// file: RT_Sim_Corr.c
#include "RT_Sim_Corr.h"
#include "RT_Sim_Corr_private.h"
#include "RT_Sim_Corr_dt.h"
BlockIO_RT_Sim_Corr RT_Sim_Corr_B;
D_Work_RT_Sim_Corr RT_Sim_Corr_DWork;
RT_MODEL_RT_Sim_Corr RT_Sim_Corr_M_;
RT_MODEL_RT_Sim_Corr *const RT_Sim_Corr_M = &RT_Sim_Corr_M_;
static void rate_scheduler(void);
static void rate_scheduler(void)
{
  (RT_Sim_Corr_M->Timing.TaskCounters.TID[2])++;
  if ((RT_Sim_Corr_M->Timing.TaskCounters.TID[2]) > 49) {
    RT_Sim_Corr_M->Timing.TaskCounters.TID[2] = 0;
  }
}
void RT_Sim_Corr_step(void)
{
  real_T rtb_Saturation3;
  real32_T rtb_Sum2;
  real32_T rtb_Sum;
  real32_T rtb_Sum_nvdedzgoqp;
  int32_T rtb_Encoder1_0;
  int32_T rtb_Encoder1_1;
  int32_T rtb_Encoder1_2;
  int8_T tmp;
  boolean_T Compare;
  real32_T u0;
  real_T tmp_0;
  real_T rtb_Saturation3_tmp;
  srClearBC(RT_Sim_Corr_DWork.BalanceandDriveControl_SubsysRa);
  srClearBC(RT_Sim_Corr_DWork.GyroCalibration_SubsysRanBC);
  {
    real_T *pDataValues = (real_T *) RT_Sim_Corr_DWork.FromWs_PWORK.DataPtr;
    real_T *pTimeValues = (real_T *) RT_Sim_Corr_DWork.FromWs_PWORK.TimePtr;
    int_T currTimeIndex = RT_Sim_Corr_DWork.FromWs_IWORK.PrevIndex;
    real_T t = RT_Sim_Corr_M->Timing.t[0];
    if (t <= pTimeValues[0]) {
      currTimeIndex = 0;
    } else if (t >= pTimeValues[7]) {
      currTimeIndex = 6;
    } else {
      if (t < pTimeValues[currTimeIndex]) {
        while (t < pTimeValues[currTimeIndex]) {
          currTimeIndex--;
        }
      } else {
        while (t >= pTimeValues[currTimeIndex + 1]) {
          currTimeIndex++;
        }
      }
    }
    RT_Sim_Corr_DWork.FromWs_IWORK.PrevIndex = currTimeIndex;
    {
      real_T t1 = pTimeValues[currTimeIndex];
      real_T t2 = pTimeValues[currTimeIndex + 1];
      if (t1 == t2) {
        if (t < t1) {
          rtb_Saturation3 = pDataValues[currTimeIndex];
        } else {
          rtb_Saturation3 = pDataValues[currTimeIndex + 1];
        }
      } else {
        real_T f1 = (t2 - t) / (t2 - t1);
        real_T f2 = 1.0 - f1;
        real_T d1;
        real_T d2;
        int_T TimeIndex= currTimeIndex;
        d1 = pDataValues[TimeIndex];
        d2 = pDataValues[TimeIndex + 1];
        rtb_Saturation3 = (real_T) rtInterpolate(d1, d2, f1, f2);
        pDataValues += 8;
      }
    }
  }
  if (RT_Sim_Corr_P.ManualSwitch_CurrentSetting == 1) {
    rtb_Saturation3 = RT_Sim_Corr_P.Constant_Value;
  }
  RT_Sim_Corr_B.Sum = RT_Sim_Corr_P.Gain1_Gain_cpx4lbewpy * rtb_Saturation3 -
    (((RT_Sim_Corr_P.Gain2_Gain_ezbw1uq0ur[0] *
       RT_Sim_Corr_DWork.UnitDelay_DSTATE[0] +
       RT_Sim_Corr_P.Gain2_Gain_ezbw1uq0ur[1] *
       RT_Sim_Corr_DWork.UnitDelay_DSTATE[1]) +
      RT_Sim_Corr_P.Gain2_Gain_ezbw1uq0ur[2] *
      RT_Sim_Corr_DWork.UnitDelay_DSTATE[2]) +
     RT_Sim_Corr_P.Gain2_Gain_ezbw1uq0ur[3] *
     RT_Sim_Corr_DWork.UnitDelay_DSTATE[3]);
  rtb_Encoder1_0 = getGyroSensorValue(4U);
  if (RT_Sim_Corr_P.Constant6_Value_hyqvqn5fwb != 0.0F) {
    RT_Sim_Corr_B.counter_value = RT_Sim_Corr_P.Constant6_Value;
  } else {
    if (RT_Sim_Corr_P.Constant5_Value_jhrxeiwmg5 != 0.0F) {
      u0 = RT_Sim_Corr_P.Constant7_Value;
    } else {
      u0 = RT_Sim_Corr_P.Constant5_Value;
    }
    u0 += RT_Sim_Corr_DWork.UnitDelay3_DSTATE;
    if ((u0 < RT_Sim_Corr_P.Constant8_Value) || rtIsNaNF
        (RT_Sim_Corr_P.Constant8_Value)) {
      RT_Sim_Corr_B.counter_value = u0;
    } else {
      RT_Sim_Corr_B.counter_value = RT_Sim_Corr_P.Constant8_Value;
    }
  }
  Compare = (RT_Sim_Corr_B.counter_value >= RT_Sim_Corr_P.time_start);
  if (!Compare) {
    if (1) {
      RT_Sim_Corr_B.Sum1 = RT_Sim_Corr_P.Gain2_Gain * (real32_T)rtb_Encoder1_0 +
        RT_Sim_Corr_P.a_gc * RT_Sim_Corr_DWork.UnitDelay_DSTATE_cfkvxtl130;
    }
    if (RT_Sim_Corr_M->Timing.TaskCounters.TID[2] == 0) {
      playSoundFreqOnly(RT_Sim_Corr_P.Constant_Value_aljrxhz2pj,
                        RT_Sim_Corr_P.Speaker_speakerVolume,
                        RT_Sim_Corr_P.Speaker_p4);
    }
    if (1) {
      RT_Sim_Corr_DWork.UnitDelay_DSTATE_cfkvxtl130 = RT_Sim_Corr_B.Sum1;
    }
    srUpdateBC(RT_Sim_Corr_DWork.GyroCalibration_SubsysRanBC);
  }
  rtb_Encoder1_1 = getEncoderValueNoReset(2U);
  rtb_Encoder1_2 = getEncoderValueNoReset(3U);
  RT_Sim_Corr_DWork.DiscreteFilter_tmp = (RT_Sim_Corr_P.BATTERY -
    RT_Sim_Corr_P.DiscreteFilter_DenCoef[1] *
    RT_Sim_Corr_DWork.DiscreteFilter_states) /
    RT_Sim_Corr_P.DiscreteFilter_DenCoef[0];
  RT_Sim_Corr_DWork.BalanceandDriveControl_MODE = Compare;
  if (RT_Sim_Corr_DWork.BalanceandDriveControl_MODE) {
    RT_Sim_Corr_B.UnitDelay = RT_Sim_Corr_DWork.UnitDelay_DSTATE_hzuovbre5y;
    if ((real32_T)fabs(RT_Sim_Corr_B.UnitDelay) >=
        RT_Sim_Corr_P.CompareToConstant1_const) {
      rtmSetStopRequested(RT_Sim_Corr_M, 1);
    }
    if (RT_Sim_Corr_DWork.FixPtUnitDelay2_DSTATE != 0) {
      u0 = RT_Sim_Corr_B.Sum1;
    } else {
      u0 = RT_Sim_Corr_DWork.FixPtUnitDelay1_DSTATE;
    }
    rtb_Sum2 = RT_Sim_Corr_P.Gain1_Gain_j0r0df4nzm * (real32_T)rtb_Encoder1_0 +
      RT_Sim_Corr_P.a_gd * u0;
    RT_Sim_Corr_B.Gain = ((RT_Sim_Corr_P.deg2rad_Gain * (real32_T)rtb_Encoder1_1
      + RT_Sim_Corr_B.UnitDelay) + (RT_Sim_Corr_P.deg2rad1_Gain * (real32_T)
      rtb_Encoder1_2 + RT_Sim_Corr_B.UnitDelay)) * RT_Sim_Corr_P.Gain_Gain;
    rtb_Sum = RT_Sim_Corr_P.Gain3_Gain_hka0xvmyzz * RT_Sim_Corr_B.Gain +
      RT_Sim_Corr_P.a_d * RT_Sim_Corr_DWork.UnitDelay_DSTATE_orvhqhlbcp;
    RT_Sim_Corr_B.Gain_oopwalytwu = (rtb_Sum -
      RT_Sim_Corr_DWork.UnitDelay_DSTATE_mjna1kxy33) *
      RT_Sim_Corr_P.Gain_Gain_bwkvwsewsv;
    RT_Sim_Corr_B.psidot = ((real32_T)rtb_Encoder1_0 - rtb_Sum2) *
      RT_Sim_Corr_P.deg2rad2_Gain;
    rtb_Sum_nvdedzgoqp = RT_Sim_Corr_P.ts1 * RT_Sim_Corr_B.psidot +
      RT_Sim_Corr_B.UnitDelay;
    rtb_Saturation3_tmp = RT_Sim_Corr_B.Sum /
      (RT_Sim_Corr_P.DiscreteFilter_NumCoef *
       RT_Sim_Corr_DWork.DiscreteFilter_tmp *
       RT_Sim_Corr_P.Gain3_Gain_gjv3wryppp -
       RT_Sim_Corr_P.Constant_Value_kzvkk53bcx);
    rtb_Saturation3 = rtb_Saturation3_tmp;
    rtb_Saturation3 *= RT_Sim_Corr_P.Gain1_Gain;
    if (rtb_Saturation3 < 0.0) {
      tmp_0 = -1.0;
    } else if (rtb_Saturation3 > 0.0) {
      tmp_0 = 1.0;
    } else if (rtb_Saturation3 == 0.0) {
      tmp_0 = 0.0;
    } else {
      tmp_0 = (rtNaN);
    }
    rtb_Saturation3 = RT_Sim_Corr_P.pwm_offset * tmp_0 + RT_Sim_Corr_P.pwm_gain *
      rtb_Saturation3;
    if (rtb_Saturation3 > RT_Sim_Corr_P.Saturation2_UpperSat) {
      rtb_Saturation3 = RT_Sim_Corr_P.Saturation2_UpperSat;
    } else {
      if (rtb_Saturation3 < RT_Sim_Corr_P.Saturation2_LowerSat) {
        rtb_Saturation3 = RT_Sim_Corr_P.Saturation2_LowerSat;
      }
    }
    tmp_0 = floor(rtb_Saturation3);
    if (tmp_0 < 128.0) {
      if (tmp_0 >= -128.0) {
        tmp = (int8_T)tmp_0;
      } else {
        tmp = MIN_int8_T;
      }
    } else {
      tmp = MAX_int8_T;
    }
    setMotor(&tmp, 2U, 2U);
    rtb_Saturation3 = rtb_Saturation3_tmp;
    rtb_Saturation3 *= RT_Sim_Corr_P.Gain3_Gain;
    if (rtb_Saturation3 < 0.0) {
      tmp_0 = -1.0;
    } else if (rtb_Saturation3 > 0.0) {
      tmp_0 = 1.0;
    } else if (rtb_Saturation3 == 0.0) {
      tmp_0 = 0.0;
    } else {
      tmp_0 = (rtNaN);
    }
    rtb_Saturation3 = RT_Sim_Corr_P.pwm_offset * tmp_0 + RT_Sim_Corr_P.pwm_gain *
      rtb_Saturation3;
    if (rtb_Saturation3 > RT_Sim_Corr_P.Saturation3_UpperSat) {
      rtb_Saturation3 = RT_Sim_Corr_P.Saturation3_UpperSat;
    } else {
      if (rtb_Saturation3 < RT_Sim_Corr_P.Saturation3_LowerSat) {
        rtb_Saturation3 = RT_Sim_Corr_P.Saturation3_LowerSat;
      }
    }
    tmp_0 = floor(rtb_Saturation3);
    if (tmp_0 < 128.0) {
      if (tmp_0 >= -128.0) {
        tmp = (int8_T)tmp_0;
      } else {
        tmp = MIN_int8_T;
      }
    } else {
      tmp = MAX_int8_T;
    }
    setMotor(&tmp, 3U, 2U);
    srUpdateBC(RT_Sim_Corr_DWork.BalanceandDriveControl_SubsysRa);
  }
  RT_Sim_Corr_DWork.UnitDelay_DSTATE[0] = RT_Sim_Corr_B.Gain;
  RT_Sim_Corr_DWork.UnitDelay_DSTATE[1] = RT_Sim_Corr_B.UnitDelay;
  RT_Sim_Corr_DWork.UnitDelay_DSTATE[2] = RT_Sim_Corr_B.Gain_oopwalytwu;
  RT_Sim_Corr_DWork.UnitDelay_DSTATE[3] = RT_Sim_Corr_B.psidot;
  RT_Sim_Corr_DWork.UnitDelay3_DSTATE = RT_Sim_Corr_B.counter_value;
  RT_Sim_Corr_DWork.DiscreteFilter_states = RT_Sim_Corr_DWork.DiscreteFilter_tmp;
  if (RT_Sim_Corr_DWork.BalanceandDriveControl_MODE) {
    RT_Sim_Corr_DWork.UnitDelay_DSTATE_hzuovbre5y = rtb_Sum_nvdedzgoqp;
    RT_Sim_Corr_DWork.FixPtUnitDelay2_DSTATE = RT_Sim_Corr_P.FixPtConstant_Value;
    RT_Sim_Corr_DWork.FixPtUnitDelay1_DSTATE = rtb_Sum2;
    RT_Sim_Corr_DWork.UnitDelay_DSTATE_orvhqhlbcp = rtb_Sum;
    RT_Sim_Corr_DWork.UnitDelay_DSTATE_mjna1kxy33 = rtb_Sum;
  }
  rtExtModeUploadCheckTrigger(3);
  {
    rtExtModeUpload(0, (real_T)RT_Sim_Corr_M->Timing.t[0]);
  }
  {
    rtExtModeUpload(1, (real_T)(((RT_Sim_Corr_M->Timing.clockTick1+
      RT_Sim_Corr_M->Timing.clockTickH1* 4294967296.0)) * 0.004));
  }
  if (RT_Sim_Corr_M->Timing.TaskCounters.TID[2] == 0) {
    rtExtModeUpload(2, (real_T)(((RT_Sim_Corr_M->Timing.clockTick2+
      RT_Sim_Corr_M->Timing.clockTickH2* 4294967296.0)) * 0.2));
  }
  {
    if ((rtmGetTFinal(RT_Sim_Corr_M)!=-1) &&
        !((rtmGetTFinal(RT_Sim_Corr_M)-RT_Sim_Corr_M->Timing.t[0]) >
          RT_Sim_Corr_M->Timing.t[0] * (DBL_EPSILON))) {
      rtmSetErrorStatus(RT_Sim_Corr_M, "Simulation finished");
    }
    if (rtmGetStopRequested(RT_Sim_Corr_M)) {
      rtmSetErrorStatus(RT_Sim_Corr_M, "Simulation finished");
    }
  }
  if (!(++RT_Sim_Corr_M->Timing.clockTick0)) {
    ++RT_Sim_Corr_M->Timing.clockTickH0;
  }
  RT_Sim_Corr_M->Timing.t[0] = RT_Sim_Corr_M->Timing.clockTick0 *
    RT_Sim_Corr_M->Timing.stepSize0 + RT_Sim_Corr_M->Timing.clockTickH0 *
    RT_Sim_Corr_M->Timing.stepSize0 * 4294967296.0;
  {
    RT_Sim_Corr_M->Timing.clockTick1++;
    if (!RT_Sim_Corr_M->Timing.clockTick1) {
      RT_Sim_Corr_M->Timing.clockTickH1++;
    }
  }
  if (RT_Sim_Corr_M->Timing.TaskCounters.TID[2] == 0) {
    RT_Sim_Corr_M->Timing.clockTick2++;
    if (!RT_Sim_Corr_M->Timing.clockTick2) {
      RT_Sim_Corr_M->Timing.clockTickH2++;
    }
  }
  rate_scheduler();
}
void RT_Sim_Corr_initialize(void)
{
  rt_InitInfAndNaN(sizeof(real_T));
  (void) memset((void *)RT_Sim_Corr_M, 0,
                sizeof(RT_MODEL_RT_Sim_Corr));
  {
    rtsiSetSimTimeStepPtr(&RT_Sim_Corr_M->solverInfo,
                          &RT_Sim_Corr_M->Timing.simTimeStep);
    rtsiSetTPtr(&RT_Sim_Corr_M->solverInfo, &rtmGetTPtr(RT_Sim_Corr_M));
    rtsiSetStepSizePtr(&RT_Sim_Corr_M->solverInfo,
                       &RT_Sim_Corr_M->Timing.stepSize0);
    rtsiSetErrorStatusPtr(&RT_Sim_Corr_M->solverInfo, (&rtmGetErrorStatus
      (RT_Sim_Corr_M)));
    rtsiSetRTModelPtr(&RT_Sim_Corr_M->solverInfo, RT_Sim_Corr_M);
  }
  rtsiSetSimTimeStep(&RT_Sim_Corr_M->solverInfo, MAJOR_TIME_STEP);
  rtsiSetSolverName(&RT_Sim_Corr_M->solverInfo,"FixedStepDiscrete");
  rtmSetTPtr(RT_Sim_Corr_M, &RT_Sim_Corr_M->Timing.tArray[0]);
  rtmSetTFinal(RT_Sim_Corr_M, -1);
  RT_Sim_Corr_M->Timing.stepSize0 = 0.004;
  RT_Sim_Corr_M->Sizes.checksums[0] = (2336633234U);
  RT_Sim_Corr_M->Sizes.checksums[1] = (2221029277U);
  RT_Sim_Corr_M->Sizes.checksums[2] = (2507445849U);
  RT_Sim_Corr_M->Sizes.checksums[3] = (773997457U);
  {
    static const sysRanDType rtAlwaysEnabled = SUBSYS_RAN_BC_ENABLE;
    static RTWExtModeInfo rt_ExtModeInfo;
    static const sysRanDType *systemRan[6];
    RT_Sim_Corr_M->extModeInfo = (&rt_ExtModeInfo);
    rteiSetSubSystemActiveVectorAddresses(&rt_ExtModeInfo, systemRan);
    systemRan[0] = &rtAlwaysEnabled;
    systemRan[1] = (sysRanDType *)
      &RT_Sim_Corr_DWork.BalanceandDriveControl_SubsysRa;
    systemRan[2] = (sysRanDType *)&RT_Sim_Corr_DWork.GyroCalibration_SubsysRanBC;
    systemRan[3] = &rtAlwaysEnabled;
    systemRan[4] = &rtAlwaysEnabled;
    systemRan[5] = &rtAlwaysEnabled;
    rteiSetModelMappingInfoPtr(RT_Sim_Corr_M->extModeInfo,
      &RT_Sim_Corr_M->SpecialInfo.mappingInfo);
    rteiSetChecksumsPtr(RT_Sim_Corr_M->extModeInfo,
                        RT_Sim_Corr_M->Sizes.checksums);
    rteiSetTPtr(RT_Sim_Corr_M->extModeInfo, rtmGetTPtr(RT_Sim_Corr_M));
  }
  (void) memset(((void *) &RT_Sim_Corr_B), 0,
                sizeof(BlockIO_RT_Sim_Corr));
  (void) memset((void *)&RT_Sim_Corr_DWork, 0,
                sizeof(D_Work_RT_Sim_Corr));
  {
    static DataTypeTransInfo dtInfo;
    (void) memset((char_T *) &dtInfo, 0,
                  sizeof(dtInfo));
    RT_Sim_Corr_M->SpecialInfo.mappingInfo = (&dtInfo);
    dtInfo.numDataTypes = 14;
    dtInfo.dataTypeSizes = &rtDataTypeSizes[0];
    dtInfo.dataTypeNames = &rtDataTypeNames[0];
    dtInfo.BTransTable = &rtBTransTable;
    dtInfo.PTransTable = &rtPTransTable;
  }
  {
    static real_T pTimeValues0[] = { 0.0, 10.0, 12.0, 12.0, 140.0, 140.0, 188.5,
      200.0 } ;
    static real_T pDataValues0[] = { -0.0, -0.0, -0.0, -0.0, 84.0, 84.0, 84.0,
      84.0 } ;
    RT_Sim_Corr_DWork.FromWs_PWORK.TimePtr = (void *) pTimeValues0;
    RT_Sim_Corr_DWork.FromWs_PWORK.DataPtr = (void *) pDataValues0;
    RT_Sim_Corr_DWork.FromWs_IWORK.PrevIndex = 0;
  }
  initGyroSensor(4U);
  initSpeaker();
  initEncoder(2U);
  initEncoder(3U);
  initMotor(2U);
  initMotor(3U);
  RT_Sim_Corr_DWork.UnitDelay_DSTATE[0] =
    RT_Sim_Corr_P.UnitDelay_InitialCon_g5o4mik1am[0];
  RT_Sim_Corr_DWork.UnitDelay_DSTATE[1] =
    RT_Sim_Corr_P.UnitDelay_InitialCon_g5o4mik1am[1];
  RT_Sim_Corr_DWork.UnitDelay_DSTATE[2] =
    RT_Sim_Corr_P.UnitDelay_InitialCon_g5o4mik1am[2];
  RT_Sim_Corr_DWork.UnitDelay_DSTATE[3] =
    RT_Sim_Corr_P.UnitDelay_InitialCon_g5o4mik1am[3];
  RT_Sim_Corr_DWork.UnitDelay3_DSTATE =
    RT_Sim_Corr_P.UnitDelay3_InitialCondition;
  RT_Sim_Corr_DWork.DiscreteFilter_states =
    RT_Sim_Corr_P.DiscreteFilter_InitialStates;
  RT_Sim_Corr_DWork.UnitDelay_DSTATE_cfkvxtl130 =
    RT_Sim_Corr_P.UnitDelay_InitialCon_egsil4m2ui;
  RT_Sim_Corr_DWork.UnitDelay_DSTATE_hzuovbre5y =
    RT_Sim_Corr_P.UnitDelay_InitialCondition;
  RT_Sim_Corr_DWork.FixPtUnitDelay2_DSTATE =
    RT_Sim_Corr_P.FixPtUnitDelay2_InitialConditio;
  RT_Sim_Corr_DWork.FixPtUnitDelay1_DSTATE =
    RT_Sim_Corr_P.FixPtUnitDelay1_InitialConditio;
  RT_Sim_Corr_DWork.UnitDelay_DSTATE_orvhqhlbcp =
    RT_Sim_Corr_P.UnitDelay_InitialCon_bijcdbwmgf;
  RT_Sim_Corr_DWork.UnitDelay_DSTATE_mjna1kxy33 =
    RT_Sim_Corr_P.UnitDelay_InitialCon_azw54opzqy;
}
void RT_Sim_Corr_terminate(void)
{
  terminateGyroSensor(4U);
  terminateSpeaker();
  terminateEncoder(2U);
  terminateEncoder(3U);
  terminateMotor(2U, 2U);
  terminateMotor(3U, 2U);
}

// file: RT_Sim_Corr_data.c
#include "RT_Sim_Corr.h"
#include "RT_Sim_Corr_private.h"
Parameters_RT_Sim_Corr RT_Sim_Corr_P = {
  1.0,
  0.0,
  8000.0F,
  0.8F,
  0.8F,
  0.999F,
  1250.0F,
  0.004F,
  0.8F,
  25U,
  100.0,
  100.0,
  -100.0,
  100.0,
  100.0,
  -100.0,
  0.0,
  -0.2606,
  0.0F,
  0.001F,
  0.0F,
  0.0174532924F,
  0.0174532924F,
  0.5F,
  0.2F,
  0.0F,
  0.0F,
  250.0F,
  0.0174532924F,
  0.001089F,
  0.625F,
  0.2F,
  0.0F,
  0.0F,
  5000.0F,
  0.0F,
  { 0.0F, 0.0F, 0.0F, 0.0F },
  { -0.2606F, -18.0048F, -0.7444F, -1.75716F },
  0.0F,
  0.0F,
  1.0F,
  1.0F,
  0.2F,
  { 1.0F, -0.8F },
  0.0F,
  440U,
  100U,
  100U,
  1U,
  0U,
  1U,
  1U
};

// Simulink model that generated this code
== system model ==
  Sum1 : Sum  Inputs=+-  <- 1: Constant8, 2: Switch#1
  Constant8 : Constant  Value=5000
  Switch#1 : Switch  Criteria=u2 ~= 0  <- 1: Constant6, 2: Constant#1, 3: MinMax#1
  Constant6 : Constant  Value=0
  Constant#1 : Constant  Value=0
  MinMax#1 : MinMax  Inputs=2  <- 1: Sum, 2: Constant8
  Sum : Sum  <- 1: UnitDelay3, 2: Switch#2
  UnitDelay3 : UnitDelay  <- 1: Switch#1
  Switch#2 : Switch  Criteria=u2 ~= 0  <- 1: Constant7, 2: Constant5, 3: Constant#2
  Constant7 : Constant
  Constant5 : Constant
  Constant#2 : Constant  Value=0
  FromWs : FromWorkspace
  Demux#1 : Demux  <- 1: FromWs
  ManualSwitch : ManualSwitch  <- 1: Constant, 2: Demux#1
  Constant : Constant  Value=0
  Sum#1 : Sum  Inputs=+-  <- 1: Gain1, 2: Gain2
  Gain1 : Gain  Gain=-0.2606  <- 1: ManualSwitch
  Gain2 : Gain  Gain="[-0.2606 -18.0048  -0.7444 -1.75716]"  Multiplication=Matrix(K*u)  <- 1: UnitDelay
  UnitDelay : UnitDelay  InitialCondition=[0; 0; 0; 0]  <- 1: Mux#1
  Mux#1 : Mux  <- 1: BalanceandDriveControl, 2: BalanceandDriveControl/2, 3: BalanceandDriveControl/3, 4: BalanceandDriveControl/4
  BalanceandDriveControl : Subsystem  <- 1: GyroCalibration, 2: DataTypeConversion#1, 3: DataTypeConversion#2, 4: DataTypeConversion#3, 5: DiscreteFilter, 6: Sum#1, 7: Sum#1, Enable: CompareToConstant#1
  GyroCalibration : Subsystem  <- 1: DataTypeConversion#1, Enable: Logic#1
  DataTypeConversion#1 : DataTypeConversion  <- 1: GyroSensor#1
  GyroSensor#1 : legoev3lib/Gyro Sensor
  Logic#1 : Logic  Operator=NOT  <- 1: CompareToConstant#1
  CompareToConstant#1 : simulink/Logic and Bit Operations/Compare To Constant  relop=>=  const=time_start  <- 1: DataTypeConversion#4
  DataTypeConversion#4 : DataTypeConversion  <- 1: Switch#1
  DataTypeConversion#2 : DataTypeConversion  <- 1: Encoder#1
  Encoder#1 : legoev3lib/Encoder
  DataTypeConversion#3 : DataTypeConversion  <- 1: Encoder1
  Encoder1 : legoev3lib/Encoder
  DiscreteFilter : DiscreteFilter  Numerator=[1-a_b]  Denominator=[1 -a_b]  <- 1: DataTypeConversion#5
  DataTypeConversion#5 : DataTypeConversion  <- 1: Constant#3
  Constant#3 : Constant  Value=BATTERY
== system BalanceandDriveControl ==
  Inport#1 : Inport
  Inport#2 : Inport
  Inport#3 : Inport
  Inport#4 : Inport
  Inport#5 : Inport
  Inport#6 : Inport
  Inport#7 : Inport
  EnablePort#1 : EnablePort
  Outport#1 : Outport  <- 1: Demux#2
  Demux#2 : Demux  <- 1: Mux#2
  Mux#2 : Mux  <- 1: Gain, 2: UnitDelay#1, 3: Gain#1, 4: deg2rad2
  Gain : Gain  Gain=1/2  <- 1: Sum#2
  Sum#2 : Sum  Inputs=++  <- 1: Sum#3, 2: Sum#4
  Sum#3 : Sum  Inputs=++  <- 1: deg2rad, 2: UnitDelay#1
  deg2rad : Gain  Gain=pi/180  <- 1: Inport#3
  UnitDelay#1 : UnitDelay  <- 1: Sum#5
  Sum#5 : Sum  Inputs=++  <- 1: Gain#2, 2: UnitDelay#1
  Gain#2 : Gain  Gain=ts1  <- 1: deg2rad2
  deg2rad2 : Gain  Gain=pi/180  <- 1: Sum2
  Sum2 : Sum  Inputs=+-  <- 1: Inport#2, 2: Sum#6
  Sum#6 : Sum  Inputs=++  <- 1: Gain#3, 2: Gain#4
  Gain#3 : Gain  Gain=1-a_gd  <- 1: Inport#2
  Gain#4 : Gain  Gain=a_gd  <- 1: UnitDelayExternalIC#1
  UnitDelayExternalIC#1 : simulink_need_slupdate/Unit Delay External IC  <- 1: Sum#6, 2: Inport#1
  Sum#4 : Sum  Inputs=++  <- 1: deg2rad1, 2: UnitDelay#1
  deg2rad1 : Gain  Gain=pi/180  <- 1: Inport#4
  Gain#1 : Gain  Gain=1/ts1  <- 1: Sum#7
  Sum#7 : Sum  Inputs=+-  <- 1: Sum#8, 2: UnitDelay#2
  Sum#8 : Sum  Inputs=++  <- 1: Gain3, 2: Gain#5
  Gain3 : Gain  Gain=1-a_d  <- 1: Gain
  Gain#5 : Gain  Gain=a_d  <- 1: UnitDelay#3
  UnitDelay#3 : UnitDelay  <- 1: Sum#8
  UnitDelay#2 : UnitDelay  <- 1: Sum#8
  Outport#2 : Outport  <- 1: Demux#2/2
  Outport#3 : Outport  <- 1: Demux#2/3
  Outport#4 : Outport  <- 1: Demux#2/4
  Stop#1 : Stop  <- 1: CompareToConstant1
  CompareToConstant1 : simulink/Logic and Bit Operations/Compare To Constant  relop=>=  const=0.8  <- 1: Abs#1
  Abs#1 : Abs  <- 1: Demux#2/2
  Motor#1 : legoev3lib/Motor  <- 1: Saturation2
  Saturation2 : Saturate  UpperLimit=100  LowerLimit=-100  <- 1: CoulombViscousFriction#1
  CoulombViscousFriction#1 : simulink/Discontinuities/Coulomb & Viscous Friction  <- 1: Gain#6
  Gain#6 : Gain  Gain=100  <- 1: Product#1
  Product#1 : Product  Inputs=*/  <- 1: Inport#6, 2: Sum#9
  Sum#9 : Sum  Inputs=+-  <- 1: Gain#7, 2: Constant#4
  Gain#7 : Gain  Gain=0.001089  <- 1: Inport#5
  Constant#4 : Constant  Value=0.625
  Motor#2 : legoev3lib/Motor  <- 1: Saturation3
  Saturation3 : Saturate  UpperLimit=100  LowerLimit=-100  <- 1: CoulombViscousFriction#2
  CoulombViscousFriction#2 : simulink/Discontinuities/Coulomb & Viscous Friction  <- 1: Gain#8
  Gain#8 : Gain  Gain=100  <- 1: Product#2
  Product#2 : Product  Inputs=*/  <- 1: Inport#7, 2: Sum#9
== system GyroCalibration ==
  Inport#8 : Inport
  EnablePort#2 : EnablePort
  Outport#5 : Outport  <- 1: Sum#10
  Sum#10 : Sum  Inputs=++  <- 1: Gain#9, 2: Gain#10
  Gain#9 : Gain  Gain=1-a_gc  <- 1: Inport#8
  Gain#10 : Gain  Gain=a_gc  <- 1: UnitDelay#4
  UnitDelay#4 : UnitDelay  <- 1: Sum#10
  Speaker#1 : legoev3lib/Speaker  <- 1: Constant#5
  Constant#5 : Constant  Value=440
